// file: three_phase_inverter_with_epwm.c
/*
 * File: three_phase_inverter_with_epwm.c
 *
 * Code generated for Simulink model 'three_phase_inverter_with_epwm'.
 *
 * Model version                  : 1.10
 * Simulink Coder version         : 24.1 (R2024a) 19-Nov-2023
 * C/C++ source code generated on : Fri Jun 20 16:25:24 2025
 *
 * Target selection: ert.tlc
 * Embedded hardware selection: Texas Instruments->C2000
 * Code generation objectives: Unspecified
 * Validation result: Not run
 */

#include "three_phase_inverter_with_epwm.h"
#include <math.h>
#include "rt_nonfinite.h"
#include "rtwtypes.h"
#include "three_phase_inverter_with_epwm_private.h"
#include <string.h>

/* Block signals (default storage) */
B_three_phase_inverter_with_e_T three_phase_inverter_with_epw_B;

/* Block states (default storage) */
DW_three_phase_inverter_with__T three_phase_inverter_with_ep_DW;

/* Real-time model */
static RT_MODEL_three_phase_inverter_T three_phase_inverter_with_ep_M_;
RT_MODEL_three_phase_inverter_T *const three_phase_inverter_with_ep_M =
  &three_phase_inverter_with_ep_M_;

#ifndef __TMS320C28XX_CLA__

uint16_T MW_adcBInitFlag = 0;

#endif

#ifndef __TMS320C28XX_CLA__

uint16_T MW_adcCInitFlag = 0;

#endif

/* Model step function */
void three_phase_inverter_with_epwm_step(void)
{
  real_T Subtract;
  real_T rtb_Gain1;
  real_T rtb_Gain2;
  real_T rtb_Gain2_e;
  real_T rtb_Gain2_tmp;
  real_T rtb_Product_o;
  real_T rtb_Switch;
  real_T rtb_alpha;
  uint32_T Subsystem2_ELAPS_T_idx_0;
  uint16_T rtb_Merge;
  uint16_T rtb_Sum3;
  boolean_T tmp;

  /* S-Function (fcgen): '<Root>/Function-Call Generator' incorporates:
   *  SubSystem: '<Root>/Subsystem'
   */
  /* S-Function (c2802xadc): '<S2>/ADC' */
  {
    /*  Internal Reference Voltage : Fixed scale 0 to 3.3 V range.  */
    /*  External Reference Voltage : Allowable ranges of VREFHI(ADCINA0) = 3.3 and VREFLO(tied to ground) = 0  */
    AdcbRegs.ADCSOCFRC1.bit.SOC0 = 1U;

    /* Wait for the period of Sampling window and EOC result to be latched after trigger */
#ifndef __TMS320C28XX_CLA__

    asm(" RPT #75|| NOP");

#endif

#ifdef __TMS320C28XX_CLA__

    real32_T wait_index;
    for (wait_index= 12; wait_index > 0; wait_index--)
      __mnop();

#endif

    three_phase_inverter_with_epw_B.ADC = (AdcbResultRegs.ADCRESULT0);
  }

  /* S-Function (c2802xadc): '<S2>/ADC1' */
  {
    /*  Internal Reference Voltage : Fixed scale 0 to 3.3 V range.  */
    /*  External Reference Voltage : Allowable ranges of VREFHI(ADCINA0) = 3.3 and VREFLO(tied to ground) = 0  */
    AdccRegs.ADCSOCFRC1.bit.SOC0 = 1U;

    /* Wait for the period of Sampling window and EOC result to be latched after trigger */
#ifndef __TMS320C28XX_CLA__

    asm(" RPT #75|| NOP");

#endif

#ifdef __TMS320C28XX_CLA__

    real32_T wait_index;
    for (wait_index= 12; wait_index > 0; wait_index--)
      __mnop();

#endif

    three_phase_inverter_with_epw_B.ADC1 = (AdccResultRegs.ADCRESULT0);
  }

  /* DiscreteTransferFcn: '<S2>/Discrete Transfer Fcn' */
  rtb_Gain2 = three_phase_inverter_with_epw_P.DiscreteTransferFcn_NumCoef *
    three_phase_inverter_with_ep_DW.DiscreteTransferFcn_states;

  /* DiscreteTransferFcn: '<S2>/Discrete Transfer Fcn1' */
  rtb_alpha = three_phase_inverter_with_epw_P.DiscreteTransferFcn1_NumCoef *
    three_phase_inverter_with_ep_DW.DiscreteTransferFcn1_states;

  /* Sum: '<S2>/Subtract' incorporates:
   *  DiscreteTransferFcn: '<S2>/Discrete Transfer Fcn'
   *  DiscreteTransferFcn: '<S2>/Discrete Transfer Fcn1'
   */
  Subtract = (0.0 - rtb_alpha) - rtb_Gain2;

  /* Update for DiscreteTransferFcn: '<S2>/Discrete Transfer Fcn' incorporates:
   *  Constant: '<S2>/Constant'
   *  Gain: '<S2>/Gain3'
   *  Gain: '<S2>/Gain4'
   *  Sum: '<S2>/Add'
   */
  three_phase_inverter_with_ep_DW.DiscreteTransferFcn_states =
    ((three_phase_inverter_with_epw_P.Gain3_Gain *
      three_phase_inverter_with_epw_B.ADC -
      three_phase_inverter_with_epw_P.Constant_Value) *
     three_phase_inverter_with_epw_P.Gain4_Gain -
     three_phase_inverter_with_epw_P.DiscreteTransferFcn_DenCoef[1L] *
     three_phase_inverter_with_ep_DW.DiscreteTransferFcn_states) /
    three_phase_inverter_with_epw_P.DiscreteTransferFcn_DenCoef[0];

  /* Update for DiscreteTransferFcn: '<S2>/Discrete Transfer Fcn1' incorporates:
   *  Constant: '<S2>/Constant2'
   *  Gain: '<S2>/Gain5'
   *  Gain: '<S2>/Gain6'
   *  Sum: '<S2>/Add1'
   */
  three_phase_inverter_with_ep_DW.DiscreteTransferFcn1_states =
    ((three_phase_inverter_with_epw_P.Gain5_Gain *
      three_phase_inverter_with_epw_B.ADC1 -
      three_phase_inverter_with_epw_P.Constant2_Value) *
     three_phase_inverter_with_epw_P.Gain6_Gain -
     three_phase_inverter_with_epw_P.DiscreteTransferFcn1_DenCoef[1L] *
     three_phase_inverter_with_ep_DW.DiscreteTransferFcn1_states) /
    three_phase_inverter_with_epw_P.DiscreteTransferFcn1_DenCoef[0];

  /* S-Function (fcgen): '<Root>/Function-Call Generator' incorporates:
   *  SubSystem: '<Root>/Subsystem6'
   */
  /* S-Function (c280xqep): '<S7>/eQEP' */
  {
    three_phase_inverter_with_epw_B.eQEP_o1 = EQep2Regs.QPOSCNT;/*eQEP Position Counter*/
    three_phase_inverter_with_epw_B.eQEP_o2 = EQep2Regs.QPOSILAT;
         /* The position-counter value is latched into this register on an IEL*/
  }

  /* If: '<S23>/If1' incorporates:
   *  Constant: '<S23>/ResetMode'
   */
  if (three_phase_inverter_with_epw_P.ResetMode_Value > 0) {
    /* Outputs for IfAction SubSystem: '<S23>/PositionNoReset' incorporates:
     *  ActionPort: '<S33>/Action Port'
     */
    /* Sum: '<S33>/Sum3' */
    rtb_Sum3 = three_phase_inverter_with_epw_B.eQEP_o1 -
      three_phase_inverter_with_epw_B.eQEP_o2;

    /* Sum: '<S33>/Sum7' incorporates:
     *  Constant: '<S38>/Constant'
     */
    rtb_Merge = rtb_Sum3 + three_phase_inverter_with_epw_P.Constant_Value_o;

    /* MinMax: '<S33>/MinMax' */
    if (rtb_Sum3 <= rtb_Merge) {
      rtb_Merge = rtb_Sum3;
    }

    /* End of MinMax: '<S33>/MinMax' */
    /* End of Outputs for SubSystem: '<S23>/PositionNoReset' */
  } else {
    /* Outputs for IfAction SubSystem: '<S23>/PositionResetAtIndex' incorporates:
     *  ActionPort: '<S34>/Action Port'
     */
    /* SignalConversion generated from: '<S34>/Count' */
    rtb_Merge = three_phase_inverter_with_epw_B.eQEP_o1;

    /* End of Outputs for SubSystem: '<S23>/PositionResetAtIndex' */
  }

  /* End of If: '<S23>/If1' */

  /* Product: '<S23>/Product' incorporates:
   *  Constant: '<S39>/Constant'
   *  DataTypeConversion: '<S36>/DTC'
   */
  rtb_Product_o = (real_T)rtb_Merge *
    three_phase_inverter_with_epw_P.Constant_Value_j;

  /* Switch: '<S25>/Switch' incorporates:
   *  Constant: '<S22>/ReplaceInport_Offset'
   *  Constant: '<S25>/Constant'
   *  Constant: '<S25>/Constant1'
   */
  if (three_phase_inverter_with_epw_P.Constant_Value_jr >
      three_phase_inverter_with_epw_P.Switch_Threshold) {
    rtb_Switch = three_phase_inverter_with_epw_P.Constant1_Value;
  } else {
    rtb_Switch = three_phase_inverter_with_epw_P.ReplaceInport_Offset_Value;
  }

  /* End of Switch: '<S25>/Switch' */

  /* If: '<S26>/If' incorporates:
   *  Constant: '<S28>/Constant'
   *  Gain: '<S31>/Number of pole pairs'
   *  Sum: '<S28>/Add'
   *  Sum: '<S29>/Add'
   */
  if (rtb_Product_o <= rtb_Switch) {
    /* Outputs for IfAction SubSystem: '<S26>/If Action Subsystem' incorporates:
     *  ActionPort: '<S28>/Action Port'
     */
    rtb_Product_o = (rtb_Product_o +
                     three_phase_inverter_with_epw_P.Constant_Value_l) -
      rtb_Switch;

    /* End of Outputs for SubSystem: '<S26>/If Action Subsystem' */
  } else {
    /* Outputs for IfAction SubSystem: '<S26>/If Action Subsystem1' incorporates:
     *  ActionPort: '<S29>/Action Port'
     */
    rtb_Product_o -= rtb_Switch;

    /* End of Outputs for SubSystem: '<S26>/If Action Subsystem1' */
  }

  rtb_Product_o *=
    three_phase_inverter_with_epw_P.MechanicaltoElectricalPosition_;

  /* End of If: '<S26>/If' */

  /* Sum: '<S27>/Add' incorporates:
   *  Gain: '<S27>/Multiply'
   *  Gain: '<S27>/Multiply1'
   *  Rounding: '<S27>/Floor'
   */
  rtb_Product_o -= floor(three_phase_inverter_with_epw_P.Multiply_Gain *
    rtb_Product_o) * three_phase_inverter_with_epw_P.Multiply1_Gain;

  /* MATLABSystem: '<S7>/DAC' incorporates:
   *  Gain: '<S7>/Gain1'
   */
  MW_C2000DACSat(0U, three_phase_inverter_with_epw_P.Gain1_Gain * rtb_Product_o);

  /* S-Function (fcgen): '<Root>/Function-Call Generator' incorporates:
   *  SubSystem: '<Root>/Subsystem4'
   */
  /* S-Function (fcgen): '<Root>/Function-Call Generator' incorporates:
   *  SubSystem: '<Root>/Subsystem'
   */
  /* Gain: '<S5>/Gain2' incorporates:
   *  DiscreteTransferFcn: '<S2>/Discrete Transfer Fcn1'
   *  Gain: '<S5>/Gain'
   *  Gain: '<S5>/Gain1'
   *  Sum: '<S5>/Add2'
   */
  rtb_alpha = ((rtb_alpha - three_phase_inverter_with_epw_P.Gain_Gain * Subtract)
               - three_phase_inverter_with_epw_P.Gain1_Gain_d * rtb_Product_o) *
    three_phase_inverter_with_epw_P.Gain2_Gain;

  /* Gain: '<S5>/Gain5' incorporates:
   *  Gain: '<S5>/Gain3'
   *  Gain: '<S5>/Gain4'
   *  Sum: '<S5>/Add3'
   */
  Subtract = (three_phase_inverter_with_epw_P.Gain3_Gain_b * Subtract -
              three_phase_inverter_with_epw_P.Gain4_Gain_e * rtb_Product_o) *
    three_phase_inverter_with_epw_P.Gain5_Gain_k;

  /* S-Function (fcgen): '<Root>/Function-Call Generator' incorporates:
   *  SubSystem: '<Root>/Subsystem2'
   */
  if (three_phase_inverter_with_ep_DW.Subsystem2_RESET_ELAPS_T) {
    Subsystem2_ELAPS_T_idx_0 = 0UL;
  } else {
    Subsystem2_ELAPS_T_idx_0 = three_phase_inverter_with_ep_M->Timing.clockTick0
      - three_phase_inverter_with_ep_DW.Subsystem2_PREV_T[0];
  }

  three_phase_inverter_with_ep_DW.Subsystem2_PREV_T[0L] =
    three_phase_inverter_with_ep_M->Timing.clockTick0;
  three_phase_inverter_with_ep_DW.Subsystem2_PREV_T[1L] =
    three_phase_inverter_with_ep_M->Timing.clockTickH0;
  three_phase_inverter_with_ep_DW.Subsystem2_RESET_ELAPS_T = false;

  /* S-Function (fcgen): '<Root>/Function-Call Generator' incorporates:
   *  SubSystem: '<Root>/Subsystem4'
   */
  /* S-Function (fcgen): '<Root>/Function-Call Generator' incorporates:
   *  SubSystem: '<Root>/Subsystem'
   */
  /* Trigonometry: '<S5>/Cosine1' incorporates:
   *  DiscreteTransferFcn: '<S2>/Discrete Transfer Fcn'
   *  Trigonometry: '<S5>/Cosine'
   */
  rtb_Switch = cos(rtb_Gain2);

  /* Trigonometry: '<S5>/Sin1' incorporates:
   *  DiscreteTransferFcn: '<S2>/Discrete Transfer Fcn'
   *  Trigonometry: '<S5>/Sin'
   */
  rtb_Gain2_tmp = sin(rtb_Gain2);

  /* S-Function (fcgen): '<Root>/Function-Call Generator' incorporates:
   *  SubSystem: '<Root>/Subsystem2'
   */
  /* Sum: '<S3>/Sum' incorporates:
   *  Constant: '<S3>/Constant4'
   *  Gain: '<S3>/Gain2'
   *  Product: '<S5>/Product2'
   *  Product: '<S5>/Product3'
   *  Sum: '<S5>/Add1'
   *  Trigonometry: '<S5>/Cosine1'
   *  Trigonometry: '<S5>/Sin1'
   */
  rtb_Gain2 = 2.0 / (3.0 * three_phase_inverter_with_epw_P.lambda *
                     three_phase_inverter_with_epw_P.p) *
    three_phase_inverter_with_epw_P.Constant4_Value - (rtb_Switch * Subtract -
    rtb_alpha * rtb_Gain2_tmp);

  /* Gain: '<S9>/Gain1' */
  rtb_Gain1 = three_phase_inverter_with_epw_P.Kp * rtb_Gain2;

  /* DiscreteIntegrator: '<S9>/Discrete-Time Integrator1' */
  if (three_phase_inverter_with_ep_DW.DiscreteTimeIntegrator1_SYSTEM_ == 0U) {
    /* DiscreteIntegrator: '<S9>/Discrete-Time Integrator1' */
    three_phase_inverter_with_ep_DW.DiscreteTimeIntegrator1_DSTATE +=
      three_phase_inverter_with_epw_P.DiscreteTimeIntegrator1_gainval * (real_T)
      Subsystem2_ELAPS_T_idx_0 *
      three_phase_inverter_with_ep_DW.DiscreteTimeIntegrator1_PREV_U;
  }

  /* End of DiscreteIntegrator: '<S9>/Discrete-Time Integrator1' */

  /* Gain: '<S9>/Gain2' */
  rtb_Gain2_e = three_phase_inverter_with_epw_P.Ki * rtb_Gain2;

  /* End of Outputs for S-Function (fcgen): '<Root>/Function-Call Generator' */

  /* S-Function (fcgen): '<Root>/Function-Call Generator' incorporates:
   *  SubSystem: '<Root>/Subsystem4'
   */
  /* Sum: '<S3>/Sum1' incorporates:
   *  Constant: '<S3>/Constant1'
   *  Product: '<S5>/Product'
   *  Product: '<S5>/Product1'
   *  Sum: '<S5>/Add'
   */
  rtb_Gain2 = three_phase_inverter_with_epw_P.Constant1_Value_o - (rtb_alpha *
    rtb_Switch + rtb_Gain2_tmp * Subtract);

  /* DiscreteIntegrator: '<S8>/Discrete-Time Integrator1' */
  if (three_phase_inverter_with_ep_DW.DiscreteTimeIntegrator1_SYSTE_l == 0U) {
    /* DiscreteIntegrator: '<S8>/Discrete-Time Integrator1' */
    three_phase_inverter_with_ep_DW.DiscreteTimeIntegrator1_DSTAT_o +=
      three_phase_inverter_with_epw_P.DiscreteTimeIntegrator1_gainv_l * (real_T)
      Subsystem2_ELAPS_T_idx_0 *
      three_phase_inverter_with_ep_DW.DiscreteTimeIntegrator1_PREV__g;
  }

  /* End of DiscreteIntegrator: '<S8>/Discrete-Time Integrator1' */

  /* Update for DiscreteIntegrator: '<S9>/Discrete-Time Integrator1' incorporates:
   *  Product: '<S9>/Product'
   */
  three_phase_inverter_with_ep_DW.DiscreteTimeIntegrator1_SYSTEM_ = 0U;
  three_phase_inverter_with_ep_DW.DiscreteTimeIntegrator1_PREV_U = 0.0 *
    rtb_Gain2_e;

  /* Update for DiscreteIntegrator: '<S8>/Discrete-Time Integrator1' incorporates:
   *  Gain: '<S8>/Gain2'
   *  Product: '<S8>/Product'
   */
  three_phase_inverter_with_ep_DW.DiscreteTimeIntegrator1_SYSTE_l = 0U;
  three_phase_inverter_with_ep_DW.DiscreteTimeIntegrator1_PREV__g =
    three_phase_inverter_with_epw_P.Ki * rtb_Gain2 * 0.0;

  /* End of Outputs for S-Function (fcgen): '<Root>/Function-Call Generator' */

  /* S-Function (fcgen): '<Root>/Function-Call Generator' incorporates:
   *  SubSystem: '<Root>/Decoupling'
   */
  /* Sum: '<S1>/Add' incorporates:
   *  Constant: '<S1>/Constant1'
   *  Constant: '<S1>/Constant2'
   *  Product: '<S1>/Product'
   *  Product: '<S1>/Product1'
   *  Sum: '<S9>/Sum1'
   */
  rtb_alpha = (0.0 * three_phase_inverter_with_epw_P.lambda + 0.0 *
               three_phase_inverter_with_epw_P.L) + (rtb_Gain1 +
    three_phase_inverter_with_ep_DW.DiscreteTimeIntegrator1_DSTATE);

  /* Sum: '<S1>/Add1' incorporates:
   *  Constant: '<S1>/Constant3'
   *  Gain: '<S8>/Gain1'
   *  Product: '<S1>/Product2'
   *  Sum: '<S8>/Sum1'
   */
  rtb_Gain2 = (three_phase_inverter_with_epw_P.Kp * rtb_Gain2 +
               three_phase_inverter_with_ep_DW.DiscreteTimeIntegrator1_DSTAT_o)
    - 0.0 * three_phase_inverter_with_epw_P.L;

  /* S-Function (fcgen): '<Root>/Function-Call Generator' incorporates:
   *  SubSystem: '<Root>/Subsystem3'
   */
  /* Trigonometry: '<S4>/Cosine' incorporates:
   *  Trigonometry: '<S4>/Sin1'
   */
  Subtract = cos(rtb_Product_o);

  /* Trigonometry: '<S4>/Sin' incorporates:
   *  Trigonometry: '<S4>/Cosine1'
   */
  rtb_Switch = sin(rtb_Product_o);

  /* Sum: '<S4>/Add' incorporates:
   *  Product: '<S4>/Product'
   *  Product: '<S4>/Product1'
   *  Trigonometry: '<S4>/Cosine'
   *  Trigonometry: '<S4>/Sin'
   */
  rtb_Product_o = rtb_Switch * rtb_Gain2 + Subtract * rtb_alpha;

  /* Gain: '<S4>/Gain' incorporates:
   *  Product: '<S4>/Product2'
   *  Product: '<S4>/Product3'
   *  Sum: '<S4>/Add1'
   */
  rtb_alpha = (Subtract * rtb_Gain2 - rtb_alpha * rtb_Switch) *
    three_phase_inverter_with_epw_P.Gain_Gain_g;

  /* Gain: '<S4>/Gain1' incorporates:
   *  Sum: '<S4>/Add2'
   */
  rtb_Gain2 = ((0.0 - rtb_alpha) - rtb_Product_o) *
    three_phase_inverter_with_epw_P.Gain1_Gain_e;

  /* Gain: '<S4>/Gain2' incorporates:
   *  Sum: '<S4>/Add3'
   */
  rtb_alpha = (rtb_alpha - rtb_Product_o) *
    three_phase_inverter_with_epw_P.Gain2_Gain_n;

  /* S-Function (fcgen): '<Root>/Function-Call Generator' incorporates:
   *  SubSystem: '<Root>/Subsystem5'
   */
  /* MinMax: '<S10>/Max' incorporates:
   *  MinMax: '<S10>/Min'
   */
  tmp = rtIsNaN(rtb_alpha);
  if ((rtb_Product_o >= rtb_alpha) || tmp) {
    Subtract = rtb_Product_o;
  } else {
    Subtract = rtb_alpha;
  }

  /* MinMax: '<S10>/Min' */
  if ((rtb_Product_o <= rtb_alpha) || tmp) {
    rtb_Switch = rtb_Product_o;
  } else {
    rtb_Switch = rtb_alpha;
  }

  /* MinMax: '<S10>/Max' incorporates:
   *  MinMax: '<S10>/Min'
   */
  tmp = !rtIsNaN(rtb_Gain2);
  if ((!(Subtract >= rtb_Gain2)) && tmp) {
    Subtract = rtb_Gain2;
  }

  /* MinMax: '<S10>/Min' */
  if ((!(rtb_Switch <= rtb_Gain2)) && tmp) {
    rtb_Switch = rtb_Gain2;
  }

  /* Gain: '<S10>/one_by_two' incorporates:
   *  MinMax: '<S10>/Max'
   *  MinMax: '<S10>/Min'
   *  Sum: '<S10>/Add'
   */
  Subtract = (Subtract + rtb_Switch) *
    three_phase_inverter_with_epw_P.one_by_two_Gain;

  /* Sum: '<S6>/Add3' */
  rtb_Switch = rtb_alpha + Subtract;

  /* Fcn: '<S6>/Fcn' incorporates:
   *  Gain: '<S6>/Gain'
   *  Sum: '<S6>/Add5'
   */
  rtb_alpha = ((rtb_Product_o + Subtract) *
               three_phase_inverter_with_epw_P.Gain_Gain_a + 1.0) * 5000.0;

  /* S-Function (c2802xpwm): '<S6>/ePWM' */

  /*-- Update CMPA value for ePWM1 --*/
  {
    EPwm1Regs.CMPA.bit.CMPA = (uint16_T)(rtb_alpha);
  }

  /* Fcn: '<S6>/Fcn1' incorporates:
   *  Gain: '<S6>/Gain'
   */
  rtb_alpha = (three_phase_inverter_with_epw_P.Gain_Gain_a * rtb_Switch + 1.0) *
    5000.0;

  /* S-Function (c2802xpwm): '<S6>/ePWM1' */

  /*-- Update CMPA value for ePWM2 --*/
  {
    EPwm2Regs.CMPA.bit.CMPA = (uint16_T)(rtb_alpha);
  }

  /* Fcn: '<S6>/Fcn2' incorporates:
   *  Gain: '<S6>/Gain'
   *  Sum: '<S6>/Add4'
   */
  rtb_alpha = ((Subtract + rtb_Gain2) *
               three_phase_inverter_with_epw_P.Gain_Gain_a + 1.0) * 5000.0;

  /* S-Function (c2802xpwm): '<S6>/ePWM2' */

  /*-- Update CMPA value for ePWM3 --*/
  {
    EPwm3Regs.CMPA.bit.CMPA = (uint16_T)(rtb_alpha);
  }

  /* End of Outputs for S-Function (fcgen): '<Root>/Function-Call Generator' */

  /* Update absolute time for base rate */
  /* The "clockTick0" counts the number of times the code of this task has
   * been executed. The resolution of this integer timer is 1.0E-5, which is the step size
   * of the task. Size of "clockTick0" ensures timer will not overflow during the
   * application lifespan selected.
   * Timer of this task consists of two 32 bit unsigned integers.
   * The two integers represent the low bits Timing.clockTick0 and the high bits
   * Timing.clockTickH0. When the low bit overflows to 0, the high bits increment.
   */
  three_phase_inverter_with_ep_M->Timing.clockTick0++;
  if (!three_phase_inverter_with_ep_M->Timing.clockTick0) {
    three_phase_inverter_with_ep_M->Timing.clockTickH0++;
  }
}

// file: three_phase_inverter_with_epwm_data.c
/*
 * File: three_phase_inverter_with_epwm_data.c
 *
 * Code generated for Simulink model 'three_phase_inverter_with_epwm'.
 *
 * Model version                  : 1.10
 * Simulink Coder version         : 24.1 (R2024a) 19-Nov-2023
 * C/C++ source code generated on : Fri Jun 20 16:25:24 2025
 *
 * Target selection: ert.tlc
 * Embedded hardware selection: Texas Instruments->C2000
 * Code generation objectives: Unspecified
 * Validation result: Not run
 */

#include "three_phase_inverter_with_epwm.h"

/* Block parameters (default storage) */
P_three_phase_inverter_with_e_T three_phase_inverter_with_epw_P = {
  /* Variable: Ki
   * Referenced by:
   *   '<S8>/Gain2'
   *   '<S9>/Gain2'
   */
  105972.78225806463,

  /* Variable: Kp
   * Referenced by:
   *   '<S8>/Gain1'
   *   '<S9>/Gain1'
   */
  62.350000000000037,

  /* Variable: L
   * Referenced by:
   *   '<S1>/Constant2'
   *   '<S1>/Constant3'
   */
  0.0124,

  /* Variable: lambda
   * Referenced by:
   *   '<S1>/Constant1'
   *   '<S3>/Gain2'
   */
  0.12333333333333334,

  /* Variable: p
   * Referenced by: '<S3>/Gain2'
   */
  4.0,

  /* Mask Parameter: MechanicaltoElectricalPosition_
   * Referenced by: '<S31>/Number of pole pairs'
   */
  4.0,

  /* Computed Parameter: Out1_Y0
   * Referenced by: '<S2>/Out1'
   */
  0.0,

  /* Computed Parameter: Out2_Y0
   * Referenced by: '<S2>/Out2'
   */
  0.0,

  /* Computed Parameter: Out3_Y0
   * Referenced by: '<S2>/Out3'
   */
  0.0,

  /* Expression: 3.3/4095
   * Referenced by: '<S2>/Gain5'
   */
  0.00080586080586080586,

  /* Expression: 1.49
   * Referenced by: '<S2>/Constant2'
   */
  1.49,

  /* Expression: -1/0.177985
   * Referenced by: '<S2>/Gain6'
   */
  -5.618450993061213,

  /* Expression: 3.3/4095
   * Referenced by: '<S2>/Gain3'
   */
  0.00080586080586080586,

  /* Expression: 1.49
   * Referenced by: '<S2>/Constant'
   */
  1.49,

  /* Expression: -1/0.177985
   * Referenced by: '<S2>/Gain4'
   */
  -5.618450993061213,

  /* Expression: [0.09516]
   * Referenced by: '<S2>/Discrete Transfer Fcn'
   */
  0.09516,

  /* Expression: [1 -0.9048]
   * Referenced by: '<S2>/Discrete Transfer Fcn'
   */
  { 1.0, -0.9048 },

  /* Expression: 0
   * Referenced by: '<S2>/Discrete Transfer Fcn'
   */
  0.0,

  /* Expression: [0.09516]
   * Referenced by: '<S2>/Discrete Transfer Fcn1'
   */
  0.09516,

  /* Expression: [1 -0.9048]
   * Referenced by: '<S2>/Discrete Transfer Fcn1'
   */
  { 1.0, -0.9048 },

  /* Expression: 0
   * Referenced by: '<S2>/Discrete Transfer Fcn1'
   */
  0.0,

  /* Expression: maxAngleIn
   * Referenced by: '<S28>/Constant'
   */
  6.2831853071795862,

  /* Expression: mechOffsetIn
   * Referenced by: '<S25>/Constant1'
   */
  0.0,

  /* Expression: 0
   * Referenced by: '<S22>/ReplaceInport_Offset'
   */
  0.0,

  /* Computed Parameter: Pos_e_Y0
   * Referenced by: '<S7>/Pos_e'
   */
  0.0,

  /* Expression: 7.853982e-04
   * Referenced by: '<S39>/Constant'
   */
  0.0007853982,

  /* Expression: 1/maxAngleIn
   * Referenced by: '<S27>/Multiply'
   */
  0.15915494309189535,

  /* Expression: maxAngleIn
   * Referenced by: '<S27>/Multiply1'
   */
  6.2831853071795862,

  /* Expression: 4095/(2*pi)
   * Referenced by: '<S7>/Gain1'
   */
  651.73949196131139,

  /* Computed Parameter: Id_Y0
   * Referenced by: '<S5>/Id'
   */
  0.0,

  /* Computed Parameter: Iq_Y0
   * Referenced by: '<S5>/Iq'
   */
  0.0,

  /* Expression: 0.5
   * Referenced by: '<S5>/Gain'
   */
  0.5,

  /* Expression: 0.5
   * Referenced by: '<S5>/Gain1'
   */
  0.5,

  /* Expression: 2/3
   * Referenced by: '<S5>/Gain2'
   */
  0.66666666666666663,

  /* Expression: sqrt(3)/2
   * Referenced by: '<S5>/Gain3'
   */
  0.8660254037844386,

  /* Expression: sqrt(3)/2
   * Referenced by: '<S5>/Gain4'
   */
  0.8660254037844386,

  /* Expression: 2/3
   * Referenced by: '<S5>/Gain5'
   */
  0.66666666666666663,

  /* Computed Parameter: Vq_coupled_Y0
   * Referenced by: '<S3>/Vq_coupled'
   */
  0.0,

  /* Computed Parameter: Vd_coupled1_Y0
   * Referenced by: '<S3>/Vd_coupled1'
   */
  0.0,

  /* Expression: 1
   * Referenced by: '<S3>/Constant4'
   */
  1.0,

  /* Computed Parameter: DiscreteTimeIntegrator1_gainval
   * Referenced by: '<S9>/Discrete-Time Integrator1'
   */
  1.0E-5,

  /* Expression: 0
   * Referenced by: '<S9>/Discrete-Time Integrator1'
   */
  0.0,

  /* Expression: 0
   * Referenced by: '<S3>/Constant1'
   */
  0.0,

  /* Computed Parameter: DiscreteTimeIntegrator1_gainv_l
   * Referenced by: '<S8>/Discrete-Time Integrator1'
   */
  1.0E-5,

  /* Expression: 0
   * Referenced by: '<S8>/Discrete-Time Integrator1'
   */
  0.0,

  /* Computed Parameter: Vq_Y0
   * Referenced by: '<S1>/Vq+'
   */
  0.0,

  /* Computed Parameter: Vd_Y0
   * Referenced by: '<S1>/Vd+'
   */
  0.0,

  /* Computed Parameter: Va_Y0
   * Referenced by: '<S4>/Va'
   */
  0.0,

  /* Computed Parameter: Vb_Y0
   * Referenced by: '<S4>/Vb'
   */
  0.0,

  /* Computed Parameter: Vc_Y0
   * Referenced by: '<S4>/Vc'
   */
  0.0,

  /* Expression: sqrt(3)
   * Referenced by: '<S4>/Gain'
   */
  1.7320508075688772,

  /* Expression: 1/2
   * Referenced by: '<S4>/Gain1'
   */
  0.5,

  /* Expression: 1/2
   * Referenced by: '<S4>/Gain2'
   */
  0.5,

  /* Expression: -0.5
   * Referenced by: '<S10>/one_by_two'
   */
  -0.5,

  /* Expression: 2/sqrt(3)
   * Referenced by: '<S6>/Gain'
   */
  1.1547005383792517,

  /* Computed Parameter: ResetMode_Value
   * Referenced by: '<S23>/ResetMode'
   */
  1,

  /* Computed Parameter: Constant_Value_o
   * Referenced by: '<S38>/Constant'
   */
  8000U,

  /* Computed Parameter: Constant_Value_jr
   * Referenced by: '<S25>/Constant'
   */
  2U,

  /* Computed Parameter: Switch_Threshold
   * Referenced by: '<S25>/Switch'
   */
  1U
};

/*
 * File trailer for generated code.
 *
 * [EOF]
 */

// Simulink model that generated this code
simulink model "three_phase_inverter_with_epwm"  (R2024a)
settings: Solver=FixedStepAuto  StartTime=0.0  StopTime=Inf  FixedStep=1e-5  RelTol=1e-3  EnableMultiTasking=on
undefined symbols (not defined in the file): DiscIntNeverNeededParam, Down, GPTRIP1SEL, Ki, Kp, L, lambda, p, TZ1, Up
libraries: c2802xlib x5, simulink x2, mcbpositiondecoderlib x2, mcbcontrolslib x1, c2837xDlib x1, eeGeneralControl x1, c280xlib x1

== system three_phase_inverter_with_epwm ==
  Decoupling : Subsystem
  Function-Call Generator : simulink/Ports & Subsystems/Function-Call Generator  sample_time=1e-5  numberOfIterations=1  DisallowWideOutput=off
  Function-Call Split : FunctionCallSplit  IconShape=distinctive  NumOutputPorts=7  OutputPortLayout=default
  Subsystem : Subsystem
  Subsystem2 : Subsystem
  Subsystem3 : Subsystem
  Subsystem4 : Subsystem
  Subsystem5 : Subsystem
  Subsystem6 : Subsystem
  wires:
  [Theta] -> Subsystem4/4(In4)
  [Ia] -> Subsystem4/1(In1)
  [Ib] -> Subsystem4/2(In2)
  [Ic] -> Subsystem4/3(In3)
  Subsystem4/2(Iq) -> [Iq]
  Subsystem4/1(Id) -> [Id]
  [Iq] -> Subsystem2/1(Iq)
  Subsystem2/1(Vq_coupled) -> Decoupling/1(Vq_coupled)
  Subsystem2/2(Vd_coupled1) -> Decoupling/2(Vd_coupled)
  [Theta] -> Subsystem3/3(In2)
  Decoupling/2(Vd*) -> Subsystem3/2(Vd)
  Decoupling/1(Vq*) -> Subsystem3/1(Vq)
  Function-Call Generator/1 -> Function-Call Split/1
  Subsystem/1(Out1) -> [Ia]
  Subsystem/2(Out2) -> [Ib]
  Subsystem/3(Out3) -> [Ic]
  Subsystem3/1(Va) -> Subsystem5/1(In1)
  Subsystem3/2(Vb) -> Subsystem5/2(In2)
  Subsystem3/3(Vc) -> Subsystem5/3(In3)
  Subsystem6/1(Pos_e) -> [Theta]
  [Id] -> Subsystem2/2(Id)
  Function-Call Split/1 -> [ADC_Current]
  Function-Call Split/2 -> [Theta_measurment]
  Function-Call Split/3 -> [Clarke_Park]
  Function-Call Split/4 -> [Current_PI_Control]
  Function-Call Split/5 -> [Decoupling]
  Function-Call Split/6 -> [Inverse_Clarke_Park]
  Function-Call Split/7 -> [SVPWM]
  [ADC_Current] -> Subsystem/Trigger
  [Theta_measurment] -> Subsystem6/Trigger
  [Clarke_Park] -> Subsystem4/Trigger
  [Current_PI_Control] -> Subsystem2/Trigger
  [Decoupling] -> Decoupling/Trigger
  [Inverse_Clarke_Park] -> Subsystem3/Trigger
  [SVPWM] -> Subsystem5/Trigger

== system three_phase_inverter_with_epwm/Decoupling ==
  Vq_coupled : Inport
  Vd_coupled : Inport  Port=2
  Trigger : TriggerPort  TriggerType=function-call  VariantControl=Variant  PortDimensions=1
  Add : Sum  Inputs=+++
  Add1 : Sum  Inputs=+-
  Constant1 : Constant  Value=lambda
  Constant2 : Constant  Value=L
  Constant3 : Constant  Value=L
  Product : Product
  Product1 : Product  Inputs=3
  Product2 : Product  Inputs=3
  Vq* : Outport
  Vd* : Outport  Port=2
  wires:
  [W_act] -> Product1/1
  Product/1 -> Add/1
  Product1/1 -> Add/2
  [W_act] -> Product2/1
  Product2/1 -> Add1/2
  Constant3/1 -> Product2/3
  Constant2/1 -> Product1/3
  Constant1/1 -> Product/2
  [Id] -> Product2/2
  [W_act] -> Product/1
  [Iq] -> Product1/2
  Vd_coupled/1 -> Add1/1
  Add1/1 -> Vd*/1  "Vd"
  Add/1 -> Vq*/1  "Vq"
  Vq_coupled/1 -> Add/3

== system three_phase_inverter_with_epwm/Subsystem ==
  Trigger : TriggerPort  TriggerType=function-call  VariantControl=(inherit)  PortDimensions=1
  ADC : c2802xlib/ADC  blkParamProc=C2000_Type4  ADCModule=B  samplingMode=Single sample mode  ADCResolution=12-bit (Single-ended input)  useSOC1=SOC0  useSOC2=SOC0_SOC1  SOCAcquisitionWindow=15  SOCTriggerSource=Software  SOCInterruptTrigger=No ADCINT  Ts=-1  dType=double  postInterrupt=off  interruptSel=ADCINT1  ADCINTContinuous=on  endma=off  chdma=1  conv1=ADCINA0  conv2=ADCINA0 and ADCINB0  conv1_Type4=ADCIN4  conv2_Type4=ADCIN0 and ADCIN1
  ADC1 : c2802xlib/ADC  blkParamProc=C2000_Type4  ADCModule=C  samplingMode=Single sample mode  ADCResolution=12-bit (Single-ended input)  useSOC1=SOC0  useSOC2=SOC0_SOC1  SOCAcquisitionWindow=15  SOCTriggerSource=Software  SOCInterruptTrigger=No ADCINT  Ts=-1  dType=double  postInterrupt=off  interruptSel=ADCINT1  ADCINTContinuous=on  endma=off  chdma=1  conv1=ADCINA0  conv2=ADCINA0 and ADCINB0  conv1_Type4=ADCIN4  conv2_Type4=ADCIN0 and ADCIN1
  Add : Sum  Inputs=+-
  Add1 : Sum  Inputs=+-
  Constant : Constant  Value=1.49
  Constant2 : Constant  Value=1.49
  Discrete Transfer Fcn : DiscreteTransferFcn  Numerator=[0.09516]  Denominator=[1 -0.9048]
  Discrete Transfer Fcn1 : DiscreteTransferFcn  Numerator=[0.09516]  Denominator=[1 -0.9048]
  Display : Display
  Display1 : Display
  Display3 : Display
  Gain3 : Gain  Gain=3.3/4095
  Gain4 : Gain  Gain=-1/0.177985
  Gain5 : Gain  Gain=3.3/4095
  Gain6 : Gain  Gain=-1/0.177985
  Scope1 : Scope
  Scope2 : Scope
  Scope4 : Scope
  Subtract : Sum  Inputs=--
  Out1 : Outport
  Out2 : Outport  Port=2
  Out3 : Outport  Port=3
  wires:
  Add/1 -> Gain4/1
  Gain3/1 -> Add/1
  Discrete Transfer Fcn/1 -> Subtract/2, Out1/1, Scope1/1, Display/1
  Subtract/1 -> Out3/1, Display3/1, Scope4/1
  Discrete Transfer Fcn1/1 -> Subtract/1, Display1/1, Out2/1, Scope2/1
  Gain6/1 -> Discrete Transfer Fcn1/1
  Constant2/1 -> Add1/2
  Add1/1 -> Gain6/1
  Constant/1 -> Add/2
  Gain4/1 -> Discrete Transfer Fcn/1
  ADC1/1 -> Gain5/1
  ADC/1 -> Gain3/1
  Gain5/1 -> Add1/1

== system three_phase_inverter_with_epwm/Subsystem2 ==
  Iq : Inport
  Id : Inport  Port=2
  Trigger : TriggerPort  TriggerType=function-call  VariantControl=(inherit)  PortDimensions=1
  Constant1 : Constant  Value=0
  Constant4 : Constant
  Gain2 : Gain  Gain=2 / ( 3 * lambda * p)
  PI_Controller_Id : Subsystem
  PI_Controller_Iq : Subsystem
  Sum : Sum  Inputs=|+-
  Sum1 : Sum  Inputs=|+-
  Vq_coupled : Outport
  Vd_coupled1 : Outport  Port=2
  wires:
  PI_Controller_Id/1(Vd_coupled) -> Vd_coupled1/1
  PI_Controller_Iq/1(Vq_coupled) -> Vq_coupled/1
  Sum/1 -> PI_Controller_Iq/1(Iq_error)
  Constant4/1 -> Gain2/1
  Gain2/1 -> Sum/1  "I_q*"
  Iq/1 -> Sum/2
  Id/1 -> Sum1/2
  Constant1/1 -> Sum1/1
  Sum1/1 -> PI_Controller_Id/1(Id_error)

== system three_phase_inverter_with_epwm/Subsystem3 ==
  Vq : Inport
  Vd : Inport  Port=2
  In2 : Inport  Port=3
  Trigger : TriggerPort  TriggerType=function-call  VariantControl=Variant  PortDimensions=1
  Add : Sum
  Add1 : Sum  Inputs=-+
  Add2 : Sum  Inputs=--
  Add3 : Sum  Inputs=+-
  Cosine : Trigonometry  Operator=cos
  Cosine1 : Trigonometry
  Gain : Gain  Gain=sqrt(3)
  Gain1 : Gain  Gain=1/2
  Gain2 : Gain  Gain=1/2
  Product{,1..3} (4 alike) : Product
  Sin : Trigonometry
  Sin1 : Trigonometry  Operator=cos
  Va : Outport
  Vb : Outport  Port=2
  Vc : Outport  Port=3
  wires:
  Add/1 -> Add3/2, Add2/2, Va/1  "V_beta"
  Product2/1 -> Add1/2
  Product3/1 -> Add1/1
  Cosine/1 -> Product/1
  Sin1/1 -> Product2/1
  Sin/1 -> Product1/1
  Product/1 -> Add/2
  Vd/1 -> Product1/2, Product2/2
  In2/1 -> Sin/1, Cosine/1, Cosine1/1, Sin1/1
  Product1/1 -> Add/1
  Cosine1/1 -> Product3/2
  Add1/1 -> Gain/1  "V_alpha"
  Vq/1 -> Product3/1, Product/2
  Gain1/1 -> Vc/1  "Vc"
  Add3/1 -> Gain2/1
  Gain/1 -> Add2/1, Add3/1
  Add2/1 -> Gain1/1
  Gain2/1 -> Vb/1  "Vb"

== system three_phase_inverter_with_epwm/Subsystem4 ==
  In1 : Inport
  In2 : Inport  Port=2
  In3 : Inport  Port=3
  In4 : Inport  Port=4
  Trigger : TriggerPort  TriggerType=function-call  VariantControl=(inherit)  PortDimensions=1
  Add : Sum
  Add1 : Sum  Inputs=-+
  Add2 : Sum  Inputs=+--
  Add3 : Sum  Inputs=+-
  Cosine : Trigonometry  Operator=cos
  Cosine1 : Trigonometry  Operator=cos
  Gain : Gain  Gain=0.5
  Gain1 : Gain  Gain=0.5
  Gain2 : Gain  Gain=2/3
  Gain3 : Gain  Gain=sqrt(3)/2
  Gain4 : Gain  Gain=sqrt(3)/2
  Gain5 : Gain  Gain=2/3
  Product{,1..3} (4 alike) : Product
  Sin : Trigonometry
  Sin1 : Trigonometry
  Id : Outport
  Iq : Outport  Port=2
  wires:
  Add1/1 -> Iq/1  "Iq"
  Add/1 -> Id/1  "Id"
  Product3/1 -> Add1/2
  Product1/1 -> Add/2
  Sin1/1 -> Product2/2
  Sin/1 -> Product1/1
  Product/1 -> Add/1
  Cosine1/1 -> Product3/1
  In1/1 -> Cosine/1, Sin/1, Cosine1/1, Sin1/1
  Product2/1 -> Add1/1
  Cosine/1 -> Product/2
  Gain5/1 -> Product3/2, Product1/2  "beta"
  Gain2/1 -> Product/1, Product2/1  "alpha"
  Add2/1 -> Gain2/1
  In2/1 -> Add2/1
  Gain/1 -> Add2/2
  In4/1 -> Gain1/1, Gain4/1
  Gain1/1 -> Add2/3
  Add3/1 -> Gain5/1
  Gain4/1 -> Add3/2
  In3/1 -> Gain/1, Gain3/1
  Gain3/1 -> Add3/1

== system three_phase_inverter_with_epwm/Subsystem5 ==
  note: (Vmin+Vmax)/2
  In1 : Inport
  In2 : Inport  Port=2
  In3 : Inport  Port=3
  Trigger : TriggerPort  TriggerType=function-call  VariantControl=(inherit)  PortDimensions=1
  Add3 : Sum  RndMeth=Simplest  OutDataTypeStr=Inherit: Same as first input
  Add4 : Sum  RndMeth=Simplest  OutDataTypeStr=Inherit: Same as first input
  Add5 : Sum  RndMeth=Simplest  OutDataTypeStr=Inherit: Same as first input
  Demux1 : Demux  Outputs=3
  Demux2 : Demux  Outputs=3
  Fcn : Fcn  Expr=(u+1)*(10000/2)
  Fcn1 : Fcn  Expr=(u+1)*(10000/2)
  Fcn2 : Fcn  Expr=(u+1)*(10000/2)
  Gain : Gain  Gain=2/sqrt(3)  RndMeth=Simplest  OutDataTypeStr=Inherit: Same as input  ParamDataTypeStr=Inherit: Same as input
  Half(Vmin+Vmax) : mcbcontrolslib/PWM Reference Generator/Modulation method/SVPWM/Half(Vmin+Vmax)  SystemSampleTime=-1  VariantActivationTime=update diagram  AllowFlexibleInterface=on  Latency=0  AutoFrameSizeCalculation=off
  Mux1 : Mux  Inputs=3
  Mux2 : Mux  Inputs=3
  Scope : Scope
  ePWM : c2802xlib/ePWM  PwmType=C2000_Type4  useModule=ePWM1  ePWMxLINKTBPRD=Not Linked  periodUnits=Clock cycles  timerSource=Specify via dialog  timerPeriod_clk=10000  timerPeriod_sec=0.0001  tbshadow=Counter equals to zero  countingMode=Up-Down  phaseActiveEnable=Disable  phaseDirection=Count down after sync  phaseActive=0  synchronizationEnable=off  dcaevt1Sync=off  dcbevt1Sync=off  synchronizationOption=Disable  dcbevt1SyncOut=off  dcaevt1SyncOut=off  cmpdSyncOut=off  cmpcSyncOut=off  cmpbSyncOut=off  zeroSyncOut=off  swfSyncOut=off  perSynchronizationOption=Counter equals to period (CTR=PRD)  clockPrescale=1  HSclockPrescale=1  enswap=off  ePWMxAStatus=on  ePWMxAactionLogic1=Do nothing  ePWMxAactionLogic2=Do nothing  ePWMxAactionLogic3=Clear  ePWMxAactionLogic4=Set  ePWMxAactionLogic5=Do nothing  ePWMxAactionLogic6=Do nothing  ePWMxACSFenable=off  ePWMxACSFvalue=Forcing disable  ePWMxASFreload=Zero  ePWMxBStatus=on  ePWMxBactionLogic1=Do nothing  ePWMxBactionLogic2=Do nothing  ePWMxBactionLogic3=Set  ePWMxBactionLogic4=Clear  ePWMxBactionLogic5=Do nothing  ePWMxBactionLogic6=Do nothing  ePWMxBCSFenable=off  ePWMxBCSFvalue=Forcing disable  ePWMxBSFreload=Zero  ePWNxBOutWay=off  ePWMxLINKCMPA=Not Linked  CMPAUnits=Clock cycles  CMPASource=Input port  CMPAValue_per=50  CMPAValue_clk=0  enCMPAshadow=Counter equals to zero (CTR=Zero)  ePWMxLINKCMPB=Not Linked  CMPBUnits=Clock cycles  CMPBSource=Specify via dialog  CMPBValue_per=50  CMPBValue_clk=32000  enCMPBshadow=Counter equals to zero (CTR=Zero)  ePWMxLINKCMPC=Not Linked  CMPCUnits=Clock cycles  CMPCSource=Specify via dialog  CMPCValue_per=50  CMPCValue_clk=32000  enCMPCshadow=Counter equals to zero (CTR=Zero)  ePWMxLINKCMPD=Not Linked  CMPDUnits=Clock cycles  CMPDSource=Specify via dialog  CMPDValue_per=50  CMPDValue_clk=32000  enCMPDshadow=Counter equals to zero (CTR=Zero)  enableDBePWMxA=on  enableDBePWMxB=on  enhalfcycle=off  DBpolarity=Active high complementary (AHC)  DBedgeDelay=Positive  DBSource_ePWMxA=ePWMxA  DBSource_ePWMxB=ePWMxA  DBPeriodUnits=Clock cycles  DBperiodSource=Specify via dialog  REDperiod=400  FEDperiod=400  REDperiod_sec=0  FEDperiod_sec=0  LoadModeDBRED=Immediate without using shadow  LoadModeDBFED=Immediate without using shadow  adcstartModuleA=off  adcrequestEventA=First event  adcstartEventA=Digital Compare Module A Event 1 start of conversion (DCAEVT1.soc)  adcstartEventA_type2=Counter equals to zero (CTR=Zero)  adcstartModuleB=off  adcrequestEventB=First event  adcstartEventB=Counter equals to zero (CTR=Zero)  adcstartEventB_type2=Counter equals to zero (CTR=Zero)  intEn=off  intPrd=First event  intSel=Counter equals to zero (CTR=Zero)  intSel_type2=Counter equals to zero (CTR=Zero)  hrpe=off  enHRPWM=off  HRPWM_LoadMode=Counter equals to period (CTR=PRD)  HRPWM_CTLMode=Duty or Period control mode  HRPWM_EDGMode=Both edge  hrpeb=off  enHRPWMB=off  HRPWM_LoadModeB=Counter equals to zero (CTR=ZERO)  HRPWM_CTLModeB=Duty or Period control mode  HRPWM_EDGModeB=Both edge  enHRDBRED=off  enHRDBFED=off  enSFO=on  enautoconv=on  chopperEnable=off  chopperFrequency=1  chopperFirstwidth=1  chopperDuty=12.5%  tripZonesource=Specify via dialog  tzselOSHT1=off  tzselOSHT2=off  tzselOSHT3=off  tzselOSHT4=off  tzselOSHT5=off  tzselOSHT6=off  tzselOSHDCAEV1=off  tzselOSHDCBEV1=off  tzselCBC1=off  tzselCBC2=off  tzselCBC3=off  tzselCBC4=off  tzselCBC5=off  tzselCBC6=off  tzselCBCDCAEV2=off  tzselCBCDCBEV2=off  enTzOstIntr=off  enTzCbcIntr=off  enTzDCAEVT1Intr=off  enTzDCAEVT2Intr=off  enTzDCBEVT1Intr=off  enTzDCBEVT2Intr=off  tzclrCBCLatch=Counter equals to zero (CTR=Zero)  ePWMxAforced=No action  ePWMxBforced=No action  DCAEVT1forced=No action  DCBEVT1forced=No action  DCAEVT2forced=No action  DCBEVT2forced=No action  dcah=Trip Zone 1 input (TZ1)  dcal=Trip Zone 2 input (TZ2)  dcbh=Trip Zone 1 input (TZ1)  dcbl=Trip Zone 2 input (TZ2)  dcah_type2=GPTRIP1SEL/(TZ1)  dcal_type2=GPTRIP1SEL/(TZ1)  dcbh_type2=GPTRIP1SEL/(TZ1)  dcbl_type2=GPTRIP1SEL/(TZ1)  gendcaevt1=Event disabled  gendcaevt2=Event disabled  gendcbevt1=Event disabled  gendcbevt2=Event disabled  dcaevt1src=DCAEVT1 with sync  dcaevt2src=DCAEVT2 with sync  dcbevt1src=DCBEVT1 with sync  dcbevt2src=DCBEVT2 with sync  pulsesel=Counter equals to zero (CTR=Zero)  blankinv=off  blankoffset=0  blankwidth=0  evsrcsel=Filtered version of DCAEVT1 (DCAEVT1FILT)  encape=off
  ePWM1 : c2802xlib/ePWM  PwmType=C2000_Type4  useModule=ePWM2  ePWMxLINKTBPRD=Not Linked  periodUnits=Clock cycles  timerSource=Specify via dialog  timerPeriod_clk=10000  timerPeriod_sec=0.0001  tbshadow=Counter equals to zero  countingMode=Up-Down  phaseActiveEnable=Disable  phaseDirection=Count down after sync  phaseActive=0  synchronizationEnable=off  dcaevt1Sync=off  dcbevt1Sync=off  synchronizationOption=Disable  dcbevt1SyncOut=off  dcaevt1SyncOut=off  cmpdSyncOut=off  cmpcSyncOut=off  cmpbSyncOut=off  zeroSyncOut=off  swfSyncOut=off  perSynchronizationOption=Counter equals to period (CTR=PRD)  clockPrescale=1  HSclockPrescale=1  enswap=off  ePWMxAStatus=on  ePWMxAactionLogic1=Do nothing  ePWMxAactionLogic2=Do nothing  ePWMxAactionLogic3=Clear  ePWMxAactionLogic4=Set  ePWMxAactionLogic5=Do nothing  ePWMxAactionLogic6=Do nothing  ePWMxACSFenable=off  ePWMxACSFvalue=Forcing disable  ePWMxASFreload=Zero  ePWMxBStatus=on  ePWMxBactionLogic1=Do nothing  ePWMxBactionLogic2=Do nothing  ePWMxBactionLogic3=Set  ePWMxBactionLogic4=Clear  ePWMxBactionLogic5=Do nothing  ePWMxBactionLogic6=Do nothing  ePWMxBCSFenable=off  ePWMxBCSFvalue=Forcing disable  ePWMxBSFreload=Zero  ePWNxBOutWay=off  ePWMxLINKCMPA=Not Linked  CMPAUnits=Clock cycles  CMPASource=Input port  CMPAValue_per=50  CMPAValue_clk=0  enCMPAshadow=Counter equals to zero (CTR=Zero)  ePWMxLINKCMPB=Not Linked  CMPBUnits=Clock cycles  CMPBSource=Specify via dialog  CMPBValue_per=50  CMPBValue_clk=32000  enCMPBshadow=Counter equals to zero (CTR=Zero)  ePWMxLINKCMPC=Not Linked  CMPCUnits=Clock cycles  CMPCSource=Specify via dialog  CMPCValue_per=50  CMPCValue_clk=32000  enCMPCshadow=Counter equals to zero (CTR=Zero)  ePWMxLINKCMPD=Not Linked  CMPDUnits=Clock cycles  CMPDSource=Specify via dialog  CMPDValue_per=50  CMPDValue_clk=32000  enCMPDshadow=Counter equals to zero (CTR=Zero)  enableDBePWMxA=on  enableDBePWMxB=on  enhalfcycle=off  DBpolarity=Active high complementary (AHC)  DBedgeDelay=Positive  DBSource_ePWMxA=ePWMxA  DBSource_ePWMxB=ePWMxA  DBPeriodUnits=Clock cycles  DBperiodSource=Specify via dialog  REDperiod=400  FEDperiod=400  REDperiod_sec=0  FEDperiod_sec=0  LoadModeDBRED=Immediate without using shadow  LoadModeDBFED=Immediate without using shadow  adcstartModuleA=off  adcrequestEventA=First event  adcstartEventA=Digital Compare Module A Event 1 start of conversion (DCAEVT1.soc)  adcstartEventA_type2=Counter equals to zero (CTR=Zero)  adcstartModuleB=off  adcrequestEventB=First event  adcstartEventB=Counter equals to zero (CTR=Zero)  adcstartEventB_type2=Counter equals to zero (CTR=Zero)  intEn=off  intPrd=First event  intSel=Counter equals to zero (CTR=Zero)  intSel_type2=Counter equals to zero (CTR=Zero)  hrpe=off  enHRPWM=off  HRPWM_LoadMode=Counter equals to period (CTR=PRD)  HRPWM_CTLMode=Duty or Period control mode  HRPWM_EDGMode=Both edge  hrpeb=off  enHRPWMB=off  HRPWM_LoadModeB=Counter equals to zero (CTR=ZERO)  HRPWM_CTLModeB=Duty or Period control mode  HRPWM_EDGModeB=Both edge  enHRDBRED=off  enHRDBFED=off  enSFO=on  enautoconv=on  chopperEnable=off  chopperFrequency=1  chopperFirstwidth=1  chopperDuty=12.5%  tripZonesource=Specify via dialog  tzselOSHT1=off  tzselOSHT2=off  tzselOSHT3=off  tzselOSHT4=off  tzselOSHT5=off  tzselOSHT6=off  tzselOSHDCAEV1=off  tzselOSHDCBEV1=off  tzselCBC1=off  tzselCBC2=off  tzselCBC3=off  tzselCBC4=off  tzselCBC5=off  tzselCBC6=off  tzselCBCDCAEV2=off  tzselCBCDCBEV2=off  enTzOstIntr=off  enTzCbcIntr=off  enTzDCAEVT1Intr=off  enTzDCAEVT2Intr=off  enTzDCBEVT1Intr=off  enTzDCBEVT2Intr=off  tzclrCBCLatch=Counter equals to zero (CTR=Zero)  ePWMxAforced=No action  ePWMxBforced=No action  DCAEVT1forced=No action  DCBEVT1forced=No action  DCAEVT2forced=No action  DCBEVT2forced=No action  dcah=Trip Zone 1 input (TZ1)  dcal=Trip Zone 2 input (TZ2)  dcbh=Trip Zone 1 input (TZ1)  dcbl=Trip Zone 2 input (TZ2)  dcah_type2=GPTRIP1SEL/(TZ1)  dcal_type2=GPTRIP1SEL/(TZ1)  dcbh_type2=GPTRIP1SEL/(TZ1)  dcbl_type2=GPTRIP1SEL/(TZ1)  gendcaevt1=Event disabled  gendcaevt2=Event disabled  gendcbevt1=Event disabled  gendcbevt2=Event disabled  dcaevt1src=DCAEVT1 with sync  dcaevt2src=DCAEVT2 with sync  dcbevt1src=DCBEVT1 with sync  dcbevt2src=DCBEVT2 with sync  pulsesel=Counter equals to zero (CTR=Zero)  blankinv=off  blankoffset=0  blankwidth=0  evsrcsel=Filtered version of DCAEVT1 (DCAEVT1FILT)  encape=off
  ePWM2 : c2802xlib/ePWM  PwmType=C2000_Type4  useModule=ePWM3  ePWMxLINKTBPRD=Not Linked  periodUnits=Clock cycles  timerSource=Specify via dialog  timerPeriod_clk=10000  timerPeriod_sec=0.0001  tbshadow=Counter equals to zero  countingMode=Up-Down  phaseActiveEnable=Disable  phaseDirection=Count down after sync  phaseActive=0  synchronizationEnable=off  dcaevt1Sync=off  dcbevt1Sync=off  synchronizationOption=Disable  dcbevt1SyncOut=off  dcaevt1SyncOut=off  cmpdSyncOut=off  cmpcSyncOut=off  cmpbSyncOut=off  zeroSyncOut=off  swfSyncOut=off  perSynchronizationOption=Counter equals to period (CTR=PRD)  clockPrescale=1  HSclockPrescale=1  enswap=off  ePWMxAStatus=on  ePWMxAactionLogic1=Do nothing  ePWMxAactionLogic2=Do nothing  ePWMxAactionLogic3=Clear  ePWMxAactionLogic4=Set  ePWMxAactionLogic5=Do nothing  ePWMxAactionLogic6=Do nothing  ePWMxACSFenable=off  ePWMxACSFvalue=Forcing disable  ePWMxASFreload=Zero  ePWMxBStatus=on  ePWMxBactionLogic1=Do nothing  ePWMxBactionLogic2=Do nothing  ePWMxBactionLogic3=Set  ePWMxBactionLogic4=Clear  ePWMxBactionLogic5=Do nothing  ePWMxBactionLogic6=Do nothing  ePWMxBCSFenable=off  ePWMxBCSFvalue=Forcing disable  ePWMxBSFreload=Zero  ePWNxBOutWay=off  ePWMxLINKCMPA=Not Linked  CMPAUnits=Clock cycles  CMPASource=Input port  CMPAValue_per=50  CMPAValue_clk=0  enCMPAshadow=Counter equals to zero (CTR=Zero)  ePWMxLINKCMPB=Not Linked  CMPBUnits=Clock cycles  CMPBSource=Specify via dialog  CMPBValue_per=50  CMPBValue_clk=32000  enCMPBshadow=Counter equals to zero (CTR=Zero)  ePWMxLINKCMPC=Not Linked  CMPCUnits=Clock cycles  CMPCSource=Specify via dialog  CMPCValue_per=50  CMPCValue_clk=32000  enCMPCshadow=Counter equals to zero (CTR=Zero)  ePWMxLINKCMPD=Not Linked  CMPDUnits=Clock cycles  CMPDSource=Specify via dialog  CMPDValue_per=50  CMPDValue_clk=32000  enCMPDshadow=Counter equals to zero (CTR=Zero)  enableDBePWMxA=on  enableDBePWMxB=on  enhalfcycle=off  DBpolarity=Active high complementary (AHC)  DBedgeDelay=Positive  DBSource_ePWMxA=ePWMxA  DBSource_ePWMxB=ePWMxA  DBPeriodUnits=Clock cycles  DBperiodSource=Specify via dialog  REDperiod=400  FEDperiod=400  REDperiod_sec=0  FEDperiod_sec=0  LoadModeDBRED=Immediate without using shadow  LoadModeDBFED=Immediate without using shadow  adcstartModuleA=off  adcrequestEventA=First event  adcstartEventA=Digital Compare Module A Event 1 start of conversion (DCAEVT1.soc)  adcstartEventA_type2=Counter equals to zero (CTR=Zero)  adcstartModuleB=off  adcrequestEventB=First event  adcstartEventB=Counter equals to zero (CTR=Zero)  adcstartEventB_type2=Counter equals to zero (CTR=Zero)  intEn=off  intPrd=First event  intSel=Counter equals to zero (CTR=Zero)  intSel_type2=Counter equals to zero (CTR=Zero)  hrpe=off  enHRPWM=off  HRPWM_LoadMode=Counter equals to period (CTR=PRD)  HRPWM_CTLMode=Duty or Period control mode  HRPWM_EDGMode=Both edge  hrpeb=off  enHRPWMB=off  HRPWM_LoadModeB=Counter equals to zero (CTR=ZERO)  HRPWM_CTLModeB=Duty or Period control mode  HRPWM_EDGModeB=Both edge  enHRDBRED=off  enHRDBFED=off  enSFO=on  enautoconv=on  chopperEnable=off  chopperFrequency=1  chopperFirstwidth=1  chopperDuty=12.5%  tripZonesource=Specify via dialog  tzselOSHT1=off  tzselOSHT2=off  tzselOSHT3=off  tzselOSHT4=off  tzselOSHT5=off  tzselOSHT6=off  tzselOSHDCAEV1=off  tzselOSHDCBEV1=off  tzselCBC1=off  tzselCBC2=off  tzselCBC3=off  tzselCBC4=off  tzselCBC5=off  tzselCBC6=off  tzselCBCDCAEV2=off  tzselCBCDCBEV2=off  enTzOstIntr=off  enTzCbcIntr=off  enTzDCAEVT1Intr=off  enTzDCAEVT2Intr=off  enTzDCBEVT1Intr=off  enTzDCBEVT2Intr=off  tzclrCBCLatch=Counter equals to zero (CTR=Zero)  ePWMxAforced=No action  ePWMxBforced=No action  DCAEVT1forced=No action  DCBEVT1forced=No action  DCAEVT2forced=No action  DCBEVT2forced=No action  dcah=Trip Zone 1 input (TZ1)  dcal=Trip Zone 2 input (TZ2)  dcbh=Trip Zone 1 input (TZ1)  dcbl=Trip Zone 2 input (TZ2)  dcah_type2=GPTRIP1SEL/(TZ1)  dcal_type2=GPTRIP1SEL/(TZ1)  dcbh_type2=GPTRIP1SEL/(TZ1)  dcbl_type2=GPTRIP1SEL/(TZ1)  gendcaevt1=Event disabled  gendcaevt2=Event disabled  gendcbevt1=Event disabled  gendcbevt2=Event disabled  dcaevt1src=DCAEVT1 with sync  dcaevt2src=DCAEVT2 with sync  dcbevt1src=DCBEVT1 with sync  dcbevt2src=DCBEVT2 with sync  pulsesel=Counter equals to zero (CTR=Zero)  blankinv=off  blankoffset=0  blankwidth=0  evsrcsel=Filtered version of DCAEVT1 (DCAEVT1FILT)  encape=off
  wires:
  Fcn/1 -> Scope/1, ePWM/1
  Half(Vmin+Vmax)/1 -> Add3/2, Add5/2, Add4/1
  Mux1/1 -> Half(Vmin+Vmax)/1, Demux1/1
  Demux2/1 -> Fcn/1
  Add4/1 -> Mux2/3
  Demux1/2 -> Add3/1
  Fcn2/1 -> ePWM2/1
  Demux2/2 -> Fcn1/1
  Fcn1/1 -> ePWM1/1
  Add3/1 -> Mux2/2
  Mux2/1 -> Gain/1
  Demux1/1 -> Add5/1
  Add5/1 -> Mux2/1
  Demux2/3 -> Fcn2/1
  Gain/1 -> Demux2/1
  Demux1/3 -> Add4/2
  In2/1 -> Mux1/2
  In1/1 -> Mux1/1
  In3/1 -> Mux1/3

== system three_phase_inverter_with_epwm/Subsystem6 ==
  Trigger : TriggerPort  TriggerType=function-call  VariantControl=(inherit)  PortDimensions=1
  DAC : c2837xDlib/DAC  channel=A  saturate=on
  Discrete Derivative : simulink/Discrete/Discrete Derivative  gainval=1.0  ICPrevScaledInput=0.0  OutMin=[]  OutMax=[]  OutDataType=fixdt(1, 16)  OutScaling=2^-10  DoSatur=off
  Gain1 : Gain  Gain=4095/(2*pi)
  "Low-Pass Filter " : eeGeneralControl/Low-Pass Filter (Discrete or Continuous)  K=1  T=1/100  B=inf  A=-inf  init_option=Inherited from block input  x0=0  Ts=-1
  Mux : Mux  Inputs=2
  Scope5 : Scope
  Scope6 : Scope  NumInputPorts=2
  Subsystem1 : Subsystem
  eQEP : c280xlib/eQEP  useModule=eQEP2  pcInputmode=Quadrature-count  externalClockrate=2x resolution: Count the rising/falling edge  swapPolarityselection=Clockwise  qdfOutputport=off  qapPolarityselection=on  qbpPolarityselection=on  qipPolarityselection=on  qspPolarityselection=off  igatePolarityselection=off  sampleTime=-1  pcOutputport=on  pcMaximumvalue=30000  indexInitializationcheck=off  indexInitializationevent=Falling edge  strobeInitializationcheck=off  strobeInitializationevent=Rising edge  softwareInitializationcheck=off  softwareInitializationsource=Set to init value at start up  softwareInitializationmode=on  pcInitialvalue=0  pcResetmode=Reset on the first index event  ieloutputport=on  indexEventlatch=Falling edge  seloutputport=off  strobeEventlatch=Rising edge  pcefOutputport=off  enableEqepcapture=off  qctmrOutputport=off  qcprdOutputport=off  captureTimerprescaler=128  upEventprescaler=128  overflowErrorflag=off  directionErrorflag=off  captureTimerposition=On position counter read  unitTimerperiod=100000000  captureTimerlatch=off  capturePeriodlatch=off  positionCounterlatch=off  soenPolarityselection=off  spselPolarityselection=Index pin is used for sync output  compareValuesource=Specify via dialog  shadowMode=Load on QPOSCNT=0  compareValue=4294967295  syncOutputwidth=1  polaritySyncoutput=Active high  watchdogEnable=off  watchdogTimer=65535  outport1Datatype=auto  outport2Datatype=auto  outport3Datatype=auto  outport4Datatype=auto  outport5Datatype=auto  outport6Datatype=auto  outport7Datatype=auto  outport8Datatype=auto  outport9Datatype=auto  outport10Datatype=auto  outport11Datatype=auto  outport12Datatype=auto  eqepinterrupt_pce=off  eqepinterrupt_qpe=off  eqepinterrupt_qdc=off  eqepinterrupt_wto=off  eqepinterrupt_pcu=off  eqepinterrupt_pco=off  eqepinterrupt_pcr=off  eqepinterrupt_pcm=off  eqepinterrupt_sel=off  eqepinterrupt_iel=off  eqepinterrupt_uto=off  pheOutputport=off  watchdogOutputport=off  outport13Datatype=auto  outport14Datatype=auto
  Pos_e : Outport
  wires:
  Subsystem1/1(Pos_e) -> Gain1/1, Pos_e/1, Scope6/1
  eQEP/1 -> Mux/1, Scope5/1
  Mux/1 -> Subsystem1/1(Pos_meas_eQEP)
  Discrete Derivative/1 -> "Low-Pass Filter "/1
  Subsystem1/2(Pos_m) -> Discrete Derivative/1
  "Low-Pass Filter "/1 -> Scope6/2
  eQEP/2 -> Mux/2
  Gain1/1 -> DAC/1

== system three_phase_inverter_with_epwm/Subsystem2/PI_Controller_Id ==
  Id_error : Inport
  Discrete-Time Integrator1 : DiscreteIntegrator  SampleTime=-1  ICPrevOutput=DiscIntNeverNeededParam  ICPrevScaledInput=DiscIntNeverNeededParam
  Gain1 : Gain  Gain=Kp
  Gain2 : Gain  Gain=Ki
  Product : Product
  Scope : Scope  NumInputPorts=2
  Scope1 : Scope
  Sum1 : Sum
  Vd_coupled : Outport
  wires:
  [Stop_d_integrator] -> Scope/2, Product/1
  Sum1/1 -> Scope1/1, Vd_coupled/1
  Product/1 -> Scope/1, Discrete-Time Integrator1/1
  Gain2/1 -> Product/2
  Discrete-Time Integrator1/1 -> Sum1/2
  Gain1/1 -> Sum1/1
  Id_error/1 -> Gain2/1, Gain1/1

== system three_phase_inverter_with_epwm/Subsystem2/PI_Controller_Iq ==
  Iq_error : Inport
  Discrete-Time Integrator1 : DiscreteIntegrator  SampleTime=-1  ICPrevOutput=DiscIntNeverNeededParam  ICPrevScaledInput=DiscIntNeverNeededParam
  Gain1 : Gain  Gain=Kp
  Gain2 : Gain  Gain=Ki
  Product : Product
  Scope : Scope  NumInputPorts=2
  Scope1 : Scope
  Sum1 : Sum
  Vq_coupled : Outport
  wires:
  Product/1 -> Scope/1, Discrete-Time Integrator1/1
  Iq_error/1 -> Gain2/1, Gain1/1
  Discrete-Time Integrator1/1 -> Sum1/2
  Gain1/1 -> Sum1/1
  Gain2/1 -> Product/2
  [Stop_q_integrator] -> Scope/2, Product/1
  Sum1/1 -> Scope1/1, Vq_coupled/1

== system three_phase_inverter_with_epwm/Subsystem6/Subsystem1 ==
  Pos_meas_eQEP : Inport
  Demux : Demux  Outputs=2
  eQEP_Decoder : Subsystem
  Pos_e : Outport  InitialOutput=0  VectorParamsAs1DForOutWhenUnconnected=off
  Pos_m : Outport  Port=2  InitialOutput=0  VectorParamsAs1DForOutWhenUnconnected=off
  wires:
  eQEP_Decoder/1(Theta_e) -> Pos_e/1
  Pos_meas_eQEP/1 -> Demux/1
  Demux/1 -> eQEP_Decoder/1(Count)
  Demux/2 -> eQEP_Decoder/2(index)
  eQEP_Decoder/2(Theta_m) -> Pos_m/1

== system three_phase_inverter_with_epwm/Subsystem6/Subsystem1/eQEP_Decoder ==
  Count : Inport
  index : Inport  Port=2
  Mechanical to Electrical Position : mcbpositiondecoderlib/Mechanical to Electrical Position  PolePairsInputType=Specify via dialog  NrPP=4  selectedRange=Radians  MechOfstInputType=Specify via dialog  mechOffsetIn=0  maxAngleIn=2*pi  InputDataType=double  VariantSelect=floating-point
  Quadrature Decoder : mcbpositiondecoderlib/Quadrature Decoder  EncoderSlitsPerRevolution=2000  EncoderCountsPerSlit=4  CounterSize=16 bits  ExternalIndexCount=on  PositionUnit=Radians  PositionDataType=double  ParameterInputType=off  CountsPerRevInverseDataType=single
  Theta_e : Outport  VectorParamsAs1DForOutWhenUnconnected=off
  Theta_m : Outport  Port=2  VectorParamsAs1DForOutWhenUnconnected=off
  wires:
  Count/1 -> Quadrature Decoder/1
  Mechanical to Electrical Position/1 -> Theta_e/1
  Quadrature Decoder/1 -> Theta_m/1, Mechanical to Electrical Position/1
  index/1 -> Quadrature Decoder/2
